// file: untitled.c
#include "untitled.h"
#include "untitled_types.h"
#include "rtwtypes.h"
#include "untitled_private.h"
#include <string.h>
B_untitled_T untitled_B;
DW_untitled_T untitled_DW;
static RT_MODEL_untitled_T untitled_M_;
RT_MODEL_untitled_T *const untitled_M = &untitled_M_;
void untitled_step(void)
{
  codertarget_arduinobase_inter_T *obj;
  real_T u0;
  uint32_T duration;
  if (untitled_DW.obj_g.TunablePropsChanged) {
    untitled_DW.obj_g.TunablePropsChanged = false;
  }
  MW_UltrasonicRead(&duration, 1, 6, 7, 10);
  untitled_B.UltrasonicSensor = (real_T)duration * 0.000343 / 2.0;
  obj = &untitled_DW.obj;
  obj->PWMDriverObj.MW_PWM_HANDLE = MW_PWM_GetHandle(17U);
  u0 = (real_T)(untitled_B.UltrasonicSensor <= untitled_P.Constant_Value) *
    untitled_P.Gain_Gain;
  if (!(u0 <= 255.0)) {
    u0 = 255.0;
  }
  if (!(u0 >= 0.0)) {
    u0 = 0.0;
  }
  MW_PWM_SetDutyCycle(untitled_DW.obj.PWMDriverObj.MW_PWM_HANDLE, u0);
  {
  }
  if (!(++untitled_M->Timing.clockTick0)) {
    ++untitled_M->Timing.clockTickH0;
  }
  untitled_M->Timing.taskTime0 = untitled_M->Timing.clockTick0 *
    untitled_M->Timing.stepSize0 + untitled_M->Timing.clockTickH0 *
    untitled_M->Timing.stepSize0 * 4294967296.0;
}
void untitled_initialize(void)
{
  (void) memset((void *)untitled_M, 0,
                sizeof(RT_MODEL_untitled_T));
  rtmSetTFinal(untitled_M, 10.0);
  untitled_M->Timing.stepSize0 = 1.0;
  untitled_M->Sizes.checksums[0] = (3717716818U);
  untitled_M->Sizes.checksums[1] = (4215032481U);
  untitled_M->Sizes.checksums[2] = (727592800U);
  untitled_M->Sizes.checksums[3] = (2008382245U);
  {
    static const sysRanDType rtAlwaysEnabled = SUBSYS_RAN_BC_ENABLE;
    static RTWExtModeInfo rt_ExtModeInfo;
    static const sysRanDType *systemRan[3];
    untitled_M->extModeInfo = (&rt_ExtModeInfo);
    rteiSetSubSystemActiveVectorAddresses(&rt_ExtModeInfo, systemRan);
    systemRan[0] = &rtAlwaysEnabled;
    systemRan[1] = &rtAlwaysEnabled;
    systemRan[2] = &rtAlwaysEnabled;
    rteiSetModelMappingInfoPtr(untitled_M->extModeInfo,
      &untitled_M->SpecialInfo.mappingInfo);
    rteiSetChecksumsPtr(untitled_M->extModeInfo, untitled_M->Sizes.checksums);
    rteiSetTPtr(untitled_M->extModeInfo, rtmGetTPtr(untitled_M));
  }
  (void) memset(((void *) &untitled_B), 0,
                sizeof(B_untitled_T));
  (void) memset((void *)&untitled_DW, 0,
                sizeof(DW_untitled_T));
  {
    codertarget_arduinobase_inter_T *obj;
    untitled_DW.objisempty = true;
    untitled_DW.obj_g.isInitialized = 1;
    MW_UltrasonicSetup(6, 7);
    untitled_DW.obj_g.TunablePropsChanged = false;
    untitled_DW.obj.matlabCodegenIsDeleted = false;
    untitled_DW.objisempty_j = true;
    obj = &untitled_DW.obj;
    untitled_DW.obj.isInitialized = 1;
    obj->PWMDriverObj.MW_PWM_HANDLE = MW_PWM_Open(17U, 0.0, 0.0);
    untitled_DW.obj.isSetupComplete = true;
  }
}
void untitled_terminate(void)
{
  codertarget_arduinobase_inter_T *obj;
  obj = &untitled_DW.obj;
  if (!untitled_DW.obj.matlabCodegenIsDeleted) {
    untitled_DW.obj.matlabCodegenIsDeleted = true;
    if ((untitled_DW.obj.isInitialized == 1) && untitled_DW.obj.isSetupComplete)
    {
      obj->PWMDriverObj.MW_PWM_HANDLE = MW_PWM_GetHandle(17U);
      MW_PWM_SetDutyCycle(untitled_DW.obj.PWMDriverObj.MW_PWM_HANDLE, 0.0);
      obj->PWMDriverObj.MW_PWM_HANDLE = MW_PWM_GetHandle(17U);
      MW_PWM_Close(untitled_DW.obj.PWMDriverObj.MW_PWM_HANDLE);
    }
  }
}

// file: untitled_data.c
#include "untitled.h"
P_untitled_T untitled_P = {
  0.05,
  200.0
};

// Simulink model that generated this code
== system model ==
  PWM : arduinolib/PWM  pinNumber=17  <- 1: Gain
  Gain : Gain  Gain=200  <- 1: DataTypeConversion#1
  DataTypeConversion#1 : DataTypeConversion  <- 1: RelationalOperator#1
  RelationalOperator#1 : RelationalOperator  Operator=<=  <- 1: UltrasonicSensor, 2: Constant
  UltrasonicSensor : arduinosensorlib/Ultrasonic Sensor
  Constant : Constant  Value=0.05
